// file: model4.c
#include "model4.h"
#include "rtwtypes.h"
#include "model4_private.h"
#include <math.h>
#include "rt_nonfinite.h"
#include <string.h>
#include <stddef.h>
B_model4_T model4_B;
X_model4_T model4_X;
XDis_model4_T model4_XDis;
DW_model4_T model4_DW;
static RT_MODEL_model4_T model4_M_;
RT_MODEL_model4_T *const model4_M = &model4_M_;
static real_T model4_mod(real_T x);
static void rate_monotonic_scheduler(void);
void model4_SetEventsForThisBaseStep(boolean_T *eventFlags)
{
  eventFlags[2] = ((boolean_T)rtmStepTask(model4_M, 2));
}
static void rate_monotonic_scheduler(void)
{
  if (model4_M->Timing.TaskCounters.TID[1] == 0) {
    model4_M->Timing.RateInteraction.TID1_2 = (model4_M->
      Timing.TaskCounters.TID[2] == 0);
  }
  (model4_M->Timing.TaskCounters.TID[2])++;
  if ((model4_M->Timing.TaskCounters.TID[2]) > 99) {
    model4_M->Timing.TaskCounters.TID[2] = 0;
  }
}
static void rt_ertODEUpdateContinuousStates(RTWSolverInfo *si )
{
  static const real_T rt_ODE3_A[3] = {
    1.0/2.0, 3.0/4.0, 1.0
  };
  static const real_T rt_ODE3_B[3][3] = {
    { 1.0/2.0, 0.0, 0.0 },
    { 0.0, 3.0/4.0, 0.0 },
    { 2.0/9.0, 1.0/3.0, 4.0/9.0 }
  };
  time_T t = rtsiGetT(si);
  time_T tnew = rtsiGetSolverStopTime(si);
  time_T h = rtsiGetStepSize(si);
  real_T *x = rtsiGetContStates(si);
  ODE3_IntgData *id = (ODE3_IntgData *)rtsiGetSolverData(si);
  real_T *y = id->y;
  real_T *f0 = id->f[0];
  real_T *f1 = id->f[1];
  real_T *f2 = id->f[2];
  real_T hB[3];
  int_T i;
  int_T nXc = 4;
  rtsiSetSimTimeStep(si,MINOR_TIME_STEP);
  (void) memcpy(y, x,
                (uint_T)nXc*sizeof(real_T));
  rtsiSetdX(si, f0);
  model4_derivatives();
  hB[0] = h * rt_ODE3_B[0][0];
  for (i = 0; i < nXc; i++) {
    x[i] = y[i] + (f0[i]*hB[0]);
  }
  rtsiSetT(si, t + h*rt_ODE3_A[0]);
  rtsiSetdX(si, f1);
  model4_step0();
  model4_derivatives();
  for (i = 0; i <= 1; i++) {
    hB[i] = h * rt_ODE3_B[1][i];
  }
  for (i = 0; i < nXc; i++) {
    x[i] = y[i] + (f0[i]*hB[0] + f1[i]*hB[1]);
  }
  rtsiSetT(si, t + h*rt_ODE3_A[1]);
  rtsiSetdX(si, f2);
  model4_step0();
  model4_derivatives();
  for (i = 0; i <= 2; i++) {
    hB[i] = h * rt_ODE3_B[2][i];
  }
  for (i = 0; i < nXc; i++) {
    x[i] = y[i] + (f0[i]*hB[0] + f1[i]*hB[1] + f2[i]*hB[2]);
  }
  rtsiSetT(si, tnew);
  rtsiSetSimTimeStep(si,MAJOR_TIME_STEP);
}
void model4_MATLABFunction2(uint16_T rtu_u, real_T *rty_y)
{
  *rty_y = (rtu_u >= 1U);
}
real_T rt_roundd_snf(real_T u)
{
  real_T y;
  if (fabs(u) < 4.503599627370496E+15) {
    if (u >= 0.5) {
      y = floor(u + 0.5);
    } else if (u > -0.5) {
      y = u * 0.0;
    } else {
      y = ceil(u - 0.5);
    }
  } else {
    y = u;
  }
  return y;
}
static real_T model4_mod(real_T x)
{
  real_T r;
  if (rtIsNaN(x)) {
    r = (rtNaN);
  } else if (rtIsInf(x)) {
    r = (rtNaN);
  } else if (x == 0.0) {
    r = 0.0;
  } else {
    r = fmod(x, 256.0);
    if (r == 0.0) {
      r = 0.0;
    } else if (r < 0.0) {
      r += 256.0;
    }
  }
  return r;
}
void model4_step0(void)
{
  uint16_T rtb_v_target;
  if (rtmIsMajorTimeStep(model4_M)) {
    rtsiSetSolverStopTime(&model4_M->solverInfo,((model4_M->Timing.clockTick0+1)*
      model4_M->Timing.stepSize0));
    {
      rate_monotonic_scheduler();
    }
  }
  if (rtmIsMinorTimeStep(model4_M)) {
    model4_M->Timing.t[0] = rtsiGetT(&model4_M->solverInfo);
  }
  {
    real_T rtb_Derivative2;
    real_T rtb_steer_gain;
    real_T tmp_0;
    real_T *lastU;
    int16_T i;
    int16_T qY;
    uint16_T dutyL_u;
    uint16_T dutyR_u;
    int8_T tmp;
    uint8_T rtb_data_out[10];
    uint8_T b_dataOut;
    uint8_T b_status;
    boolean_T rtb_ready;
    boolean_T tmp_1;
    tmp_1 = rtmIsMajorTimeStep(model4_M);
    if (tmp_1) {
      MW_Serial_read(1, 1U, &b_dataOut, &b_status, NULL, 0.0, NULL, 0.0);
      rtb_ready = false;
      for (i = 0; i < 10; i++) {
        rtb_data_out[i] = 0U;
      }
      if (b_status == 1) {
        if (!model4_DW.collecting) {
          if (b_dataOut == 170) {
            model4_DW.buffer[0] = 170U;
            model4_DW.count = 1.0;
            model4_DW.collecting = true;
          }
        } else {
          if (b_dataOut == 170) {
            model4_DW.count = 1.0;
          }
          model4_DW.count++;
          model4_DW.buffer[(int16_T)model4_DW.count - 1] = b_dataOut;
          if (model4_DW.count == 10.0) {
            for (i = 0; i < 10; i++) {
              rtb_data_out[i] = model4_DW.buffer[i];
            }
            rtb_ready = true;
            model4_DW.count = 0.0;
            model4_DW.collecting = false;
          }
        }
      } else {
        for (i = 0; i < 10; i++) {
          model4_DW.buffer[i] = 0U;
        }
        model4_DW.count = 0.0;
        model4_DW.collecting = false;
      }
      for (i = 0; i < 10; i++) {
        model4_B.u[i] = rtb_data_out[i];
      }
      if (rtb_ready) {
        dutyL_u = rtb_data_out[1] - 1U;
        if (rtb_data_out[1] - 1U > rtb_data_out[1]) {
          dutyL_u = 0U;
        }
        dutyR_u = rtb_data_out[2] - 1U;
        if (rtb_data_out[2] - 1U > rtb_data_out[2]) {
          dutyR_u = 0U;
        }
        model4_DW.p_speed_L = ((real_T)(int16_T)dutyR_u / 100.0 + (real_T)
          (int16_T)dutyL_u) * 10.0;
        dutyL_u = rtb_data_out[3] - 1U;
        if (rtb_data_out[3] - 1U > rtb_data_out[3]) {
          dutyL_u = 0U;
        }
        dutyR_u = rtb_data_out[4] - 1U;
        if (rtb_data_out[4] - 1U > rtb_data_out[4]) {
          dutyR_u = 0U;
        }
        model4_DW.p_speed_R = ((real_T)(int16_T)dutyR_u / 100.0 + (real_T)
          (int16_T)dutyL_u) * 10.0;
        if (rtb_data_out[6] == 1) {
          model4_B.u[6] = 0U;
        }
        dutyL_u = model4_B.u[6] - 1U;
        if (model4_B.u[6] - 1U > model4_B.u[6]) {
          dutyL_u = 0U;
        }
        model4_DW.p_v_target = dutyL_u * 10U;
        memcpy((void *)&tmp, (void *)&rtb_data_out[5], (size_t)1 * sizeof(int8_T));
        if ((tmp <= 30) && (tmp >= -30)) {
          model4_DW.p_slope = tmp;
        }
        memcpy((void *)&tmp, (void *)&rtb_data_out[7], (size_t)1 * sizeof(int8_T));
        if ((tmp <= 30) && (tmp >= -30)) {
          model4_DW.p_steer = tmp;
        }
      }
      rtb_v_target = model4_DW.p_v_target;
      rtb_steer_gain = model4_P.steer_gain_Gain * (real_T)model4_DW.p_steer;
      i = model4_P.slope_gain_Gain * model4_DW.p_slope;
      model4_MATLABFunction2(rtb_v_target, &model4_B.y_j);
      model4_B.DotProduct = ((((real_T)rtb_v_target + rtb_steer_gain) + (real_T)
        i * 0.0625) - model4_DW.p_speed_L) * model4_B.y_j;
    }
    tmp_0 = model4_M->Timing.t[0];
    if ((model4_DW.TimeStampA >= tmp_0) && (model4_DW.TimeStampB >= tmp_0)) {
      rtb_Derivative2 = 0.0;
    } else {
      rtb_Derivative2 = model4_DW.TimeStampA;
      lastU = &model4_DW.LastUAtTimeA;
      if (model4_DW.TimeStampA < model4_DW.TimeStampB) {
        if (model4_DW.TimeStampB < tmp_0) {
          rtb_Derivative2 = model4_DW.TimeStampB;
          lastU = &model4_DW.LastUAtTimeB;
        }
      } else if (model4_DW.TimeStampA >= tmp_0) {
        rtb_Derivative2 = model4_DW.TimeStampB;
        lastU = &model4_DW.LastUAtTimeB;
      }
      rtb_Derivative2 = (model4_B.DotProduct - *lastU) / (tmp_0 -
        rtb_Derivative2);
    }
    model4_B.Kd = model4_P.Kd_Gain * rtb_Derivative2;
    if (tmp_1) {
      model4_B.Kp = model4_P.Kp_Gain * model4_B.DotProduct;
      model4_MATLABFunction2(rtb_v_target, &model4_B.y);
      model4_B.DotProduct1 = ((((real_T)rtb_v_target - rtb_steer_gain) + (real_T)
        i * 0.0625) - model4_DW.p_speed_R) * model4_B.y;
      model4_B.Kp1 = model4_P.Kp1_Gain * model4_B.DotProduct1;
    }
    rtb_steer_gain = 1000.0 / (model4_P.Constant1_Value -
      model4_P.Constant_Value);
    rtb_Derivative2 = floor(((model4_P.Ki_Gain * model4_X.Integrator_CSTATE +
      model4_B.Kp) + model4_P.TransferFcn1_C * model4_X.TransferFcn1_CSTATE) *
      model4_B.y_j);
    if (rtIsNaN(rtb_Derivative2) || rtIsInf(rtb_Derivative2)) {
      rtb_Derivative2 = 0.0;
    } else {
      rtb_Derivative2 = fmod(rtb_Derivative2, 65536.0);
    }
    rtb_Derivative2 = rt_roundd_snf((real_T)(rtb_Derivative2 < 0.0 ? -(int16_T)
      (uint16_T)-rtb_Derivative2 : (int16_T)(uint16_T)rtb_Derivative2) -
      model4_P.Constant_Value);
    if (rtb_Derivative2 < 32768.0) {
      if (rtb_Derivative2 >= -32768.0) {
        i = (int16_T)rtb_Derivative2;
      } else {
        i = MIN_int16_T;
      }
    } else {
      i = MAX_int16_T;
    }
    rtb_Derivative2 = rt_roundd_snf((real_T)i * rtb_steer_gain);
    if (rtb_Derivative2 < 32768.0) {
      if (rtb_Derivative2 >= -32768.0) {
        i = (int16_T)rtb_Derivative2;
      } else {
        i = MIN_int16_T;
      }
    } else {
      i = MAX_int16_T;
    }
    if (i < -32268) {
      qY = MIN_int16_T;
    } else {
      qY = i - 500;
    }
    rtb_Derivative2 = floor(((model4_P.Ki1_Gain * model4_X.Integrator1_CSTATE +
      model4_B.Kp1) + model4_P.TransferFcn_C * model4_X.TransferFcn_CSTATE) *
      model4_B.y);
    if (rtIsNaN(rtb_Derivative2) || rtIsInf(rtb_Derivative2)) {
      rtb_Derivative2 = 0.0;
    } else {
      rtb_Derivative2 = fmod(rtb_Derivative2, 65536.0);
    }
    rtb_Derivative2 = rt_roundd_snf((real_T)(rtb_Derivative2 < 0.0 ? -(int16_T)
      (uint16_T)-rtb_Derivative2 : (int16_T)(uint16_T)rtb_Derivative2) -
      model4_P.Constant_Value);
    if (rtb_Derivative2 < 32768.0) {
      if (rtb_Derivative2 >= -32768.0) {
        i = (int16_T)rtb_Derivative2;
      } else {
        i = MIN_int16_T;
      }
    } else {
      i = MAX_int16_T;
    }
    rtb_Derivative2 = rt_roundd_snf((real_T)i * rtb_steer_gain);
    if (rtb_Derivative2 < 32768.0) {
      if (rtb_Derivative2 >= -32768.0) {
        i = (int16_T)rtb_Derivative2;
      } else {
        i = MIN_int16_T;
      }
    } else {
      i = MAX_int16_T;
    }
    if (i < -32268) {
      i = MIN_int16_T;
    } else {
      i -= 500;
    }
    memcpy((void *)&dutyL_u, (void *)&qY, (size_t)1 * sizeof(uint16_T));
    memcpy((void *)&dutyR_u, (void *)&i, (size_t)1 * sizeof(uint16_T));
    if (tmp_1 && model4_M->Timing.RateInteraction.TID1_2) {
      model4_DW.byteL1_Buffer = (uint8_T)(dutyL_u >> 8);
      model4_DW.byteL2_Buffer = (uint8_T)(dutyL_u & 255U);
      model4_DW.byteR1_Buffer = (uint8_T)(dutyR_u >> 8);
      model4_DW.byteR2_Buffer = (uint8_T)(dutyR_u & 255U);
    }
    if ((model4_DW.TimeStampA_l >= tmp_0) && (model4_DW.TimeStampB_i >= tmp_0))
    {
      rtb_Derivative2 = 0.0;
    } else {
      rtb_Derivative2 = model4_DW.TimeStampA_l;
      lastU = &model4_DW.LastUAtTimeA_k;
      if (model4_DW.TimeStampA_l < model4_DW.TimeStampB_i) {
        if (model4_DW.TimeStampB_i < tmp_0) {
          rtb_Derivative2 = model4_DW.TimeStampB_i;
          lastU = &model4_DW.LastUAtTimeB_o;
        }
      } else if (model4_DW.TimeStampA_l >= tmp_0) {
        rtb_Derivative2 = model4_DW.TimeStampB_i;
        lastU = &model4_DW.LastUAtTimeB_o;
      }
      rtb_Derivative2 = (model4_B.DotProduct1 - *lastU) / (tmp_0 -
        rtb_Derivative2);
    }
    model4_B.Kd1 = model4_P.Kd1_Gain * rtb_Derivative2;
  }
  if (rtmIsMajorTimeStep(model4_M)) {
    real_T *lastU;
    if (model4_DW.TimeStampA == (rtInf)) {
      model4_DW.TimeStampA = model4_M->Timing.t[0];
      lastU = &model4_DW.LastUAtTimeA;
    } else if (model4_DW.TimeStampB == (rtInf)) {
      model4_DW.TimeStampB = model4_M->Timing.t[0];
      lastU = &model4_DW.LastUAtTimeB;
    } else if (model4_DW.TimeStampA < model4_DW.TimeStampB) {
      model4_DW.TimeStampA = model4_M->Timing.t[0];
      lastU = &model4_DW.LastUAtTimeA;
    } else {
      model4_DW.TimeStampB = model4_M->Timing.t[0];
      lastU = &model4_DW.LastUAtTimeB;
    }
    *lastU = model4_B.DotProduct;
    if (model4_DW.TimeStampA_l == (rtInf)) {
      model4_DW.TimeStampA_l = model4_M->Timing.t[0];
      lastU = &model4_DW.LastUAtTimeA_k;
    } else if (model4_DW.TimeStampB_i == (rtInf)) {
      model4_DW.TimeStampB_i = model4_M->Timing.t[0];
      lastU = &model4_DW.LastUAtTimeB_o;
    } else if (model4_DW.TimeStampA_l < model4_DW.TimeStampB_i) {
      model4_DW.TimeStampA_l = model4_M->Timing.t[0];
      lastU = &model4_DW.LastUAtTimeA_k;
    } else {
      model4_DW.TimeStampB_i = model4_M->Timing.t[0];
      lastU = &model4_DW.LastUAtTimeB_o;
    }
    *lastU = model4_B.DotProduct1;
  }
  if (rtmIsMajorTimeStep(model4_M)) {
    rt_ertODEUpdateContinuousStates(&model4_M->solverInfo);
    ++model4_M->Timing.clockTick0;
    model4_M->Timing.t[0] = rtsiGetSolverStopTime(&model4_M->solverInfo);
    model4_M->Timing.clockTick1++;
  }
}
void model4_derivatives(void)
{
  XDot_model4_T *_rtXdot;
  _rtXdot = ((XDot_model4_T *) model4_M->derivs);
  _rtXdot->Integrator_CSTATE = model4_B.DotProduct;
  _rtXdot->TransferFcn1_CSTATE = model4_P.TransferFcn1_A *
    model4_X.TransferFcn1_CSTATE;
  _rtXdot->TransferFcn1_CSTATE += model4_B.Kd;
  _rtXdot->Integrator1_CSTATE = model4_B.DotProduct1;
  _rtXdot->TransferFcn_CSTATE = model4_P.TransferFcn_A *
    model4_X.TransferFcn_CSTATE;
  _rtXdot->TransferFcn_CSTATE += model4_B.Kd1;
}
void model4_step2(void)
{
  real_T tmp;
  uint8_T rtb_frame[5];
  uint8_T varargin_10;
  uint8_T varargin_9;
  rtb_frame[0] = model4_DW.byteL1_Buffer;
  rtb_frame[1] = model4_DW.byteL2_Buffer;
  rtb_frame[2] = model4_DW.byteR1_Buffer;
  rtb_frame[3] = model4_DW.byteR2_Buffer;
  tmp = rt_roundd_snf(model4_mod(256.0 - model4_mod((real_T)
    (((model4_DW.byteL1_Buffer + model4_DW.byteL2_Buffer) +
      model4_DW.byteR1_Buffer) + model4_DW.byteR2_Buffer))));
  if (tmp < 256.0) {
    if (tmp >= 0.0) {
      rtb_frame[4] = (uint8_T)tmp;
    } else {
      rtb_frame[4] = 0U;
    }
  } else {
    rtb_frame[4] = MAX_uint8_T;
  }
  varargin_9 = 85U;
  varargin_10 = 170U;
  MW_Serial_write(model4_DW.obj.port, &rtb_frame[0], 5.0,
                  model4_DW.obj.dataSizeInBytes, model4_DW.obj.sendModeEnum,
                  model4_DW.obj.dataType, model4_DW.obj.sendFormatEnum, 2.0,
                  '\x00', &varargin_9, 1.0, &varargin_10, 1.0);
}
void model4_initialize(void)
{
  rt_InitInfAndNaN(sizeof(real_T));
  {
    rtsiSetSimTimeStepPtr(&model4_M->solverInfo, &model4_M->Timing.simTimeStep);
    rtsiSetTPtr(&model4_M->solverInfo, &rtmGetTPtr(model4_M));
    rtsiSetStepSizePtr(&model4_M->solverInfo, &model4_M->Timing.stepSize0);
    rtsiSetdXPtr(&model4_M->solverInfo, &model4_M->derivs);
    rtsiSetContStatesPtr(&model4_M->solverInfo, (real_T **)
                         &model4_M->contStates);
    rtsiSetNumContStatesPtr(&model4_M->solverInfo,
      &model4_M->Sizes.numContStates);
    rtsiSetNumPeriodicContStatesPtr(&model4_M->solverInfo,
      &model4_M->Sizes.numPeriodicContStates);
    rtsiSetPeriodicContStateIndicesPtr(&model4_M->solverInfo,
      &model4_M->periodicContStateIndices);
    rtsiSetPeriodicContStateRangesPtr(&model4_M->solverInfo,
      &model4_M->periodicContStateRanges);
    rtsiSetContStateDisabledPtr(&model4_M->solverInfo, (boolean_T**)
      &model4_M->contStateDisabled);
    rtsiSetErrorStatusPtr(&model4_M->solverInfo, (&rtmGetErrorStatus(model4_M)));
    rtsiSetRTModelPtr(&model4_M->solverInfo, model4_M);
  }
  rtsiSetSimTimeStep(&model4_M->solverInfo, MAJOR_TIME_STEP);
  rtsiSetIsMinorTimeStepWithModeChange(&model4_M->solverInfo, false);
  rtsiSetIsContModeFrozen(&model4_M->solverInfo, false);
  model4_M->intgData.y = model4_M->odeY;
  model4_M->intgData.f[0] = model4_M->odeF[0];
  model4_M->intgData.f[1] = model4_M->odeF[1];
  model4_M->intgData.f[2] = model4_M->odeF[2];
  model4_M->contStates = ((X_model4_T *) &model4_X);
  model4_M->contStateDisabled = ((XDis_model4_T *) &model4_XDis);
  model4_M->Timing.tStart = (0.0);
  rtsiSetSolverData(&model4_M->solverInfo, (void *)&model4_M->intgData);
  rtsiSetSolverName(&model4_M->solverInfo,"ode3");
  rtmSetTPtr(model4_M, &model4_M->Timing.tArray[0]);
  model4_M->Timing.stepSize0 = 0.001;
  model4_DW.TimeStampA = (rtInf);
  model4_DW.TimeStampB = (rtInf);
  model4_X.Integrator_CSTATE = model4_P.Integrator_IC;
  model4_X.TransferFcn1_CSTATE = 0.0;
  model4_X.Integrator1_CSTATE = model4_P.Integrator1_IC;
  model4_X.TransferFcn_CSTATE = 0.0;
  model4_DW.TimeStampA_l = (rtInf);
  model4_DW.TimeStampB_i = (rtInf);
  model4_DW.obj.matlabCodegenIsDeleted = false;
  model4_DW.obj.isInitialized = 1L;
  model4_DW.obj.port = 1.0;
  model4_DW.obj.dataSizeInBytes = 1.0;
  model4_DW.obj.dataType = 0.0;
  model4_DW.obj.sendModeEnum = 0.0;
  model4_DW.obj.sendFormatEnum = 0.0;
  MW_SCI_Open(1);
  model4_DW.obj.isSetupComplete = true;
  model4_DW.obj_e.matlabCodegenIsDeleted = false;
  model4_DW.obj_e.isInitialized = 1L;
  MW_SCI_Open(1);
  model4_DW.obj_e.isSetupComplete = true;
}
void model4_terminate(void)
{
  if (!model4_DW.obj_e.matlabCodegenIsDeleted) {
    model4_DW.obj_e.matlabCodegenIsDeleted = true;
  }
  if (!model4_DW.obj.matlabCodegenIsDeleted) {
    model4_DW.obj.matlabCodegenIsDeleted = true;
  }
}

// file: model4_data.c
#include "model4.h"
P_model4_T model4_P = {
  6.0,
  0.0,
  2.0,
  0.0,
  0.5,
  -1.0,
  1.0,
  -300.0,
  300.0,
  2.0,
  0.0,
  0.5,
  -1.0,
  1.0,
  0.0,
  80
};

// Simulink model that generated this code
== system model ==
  Subsystem#1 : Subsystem  <- 1: MATLABFunction#1, 2: MATLABFunction#1/2, 3: MATLABFunction#1/3, 4: MATLABFunction#1/4
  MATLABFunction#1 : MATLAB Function  <- 1: DotProduct#1, 2: DotProduct#2, 3: Constant, 4: Constant1
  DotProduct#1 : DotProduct  <- 1: MATLABFunction2, 2: Sum#1
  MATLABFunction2 : MATLAB Function  <- 1: MATLABFunction#2/4
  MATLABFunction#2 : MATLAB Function  <- 1: MATLABFunction#3, 2: MATLABFunction#3/2
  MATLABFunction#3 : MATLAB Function  <- 1: SerialReceive#1, 2: SerialReceive#1/2
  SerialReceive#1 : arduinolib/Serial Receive
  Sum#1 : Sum  Inputs=+++  <- 1: Kp, 2: Ki, 3: TransferFcn1
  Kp : Gain  Gain=2  <- 1: DotProduct
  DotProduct : DotProduct  <- 1: MATLABFunction2, 2: Sum#2
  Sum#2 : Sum  Inputs=+-  <- 1: Sum#3, 2: MATLABFunction#2/2
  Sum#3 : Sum  Inputs=+++  <- 1: MATLABFunction#2/4, 2: steer_gain, 3: slope_gain
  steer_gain : Gain  Gain=6  <- 1: MATLABFunction#2/6
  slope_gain : Gain  Gain=5  <- 1: MATLABFunction#2/5
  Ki : Gain  Gain=0.5  <- 1: Integrator
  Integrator : Integrator  <- 1: DotProduct
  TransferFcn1 : TransferFcn  Denominator=[1 1]  <- 1: Kd
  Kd : Gain  Gain=0  <- 1: Derivative#1
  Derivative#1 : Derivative  <- 1: DotProduct
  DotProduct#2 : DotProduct  <- 1: MATLABFunction#4, 2: Sum#4
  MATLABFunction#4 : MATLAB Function  <- 1: MATLABFunction#2/4
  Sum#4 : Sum  Inputs=+++  <- 1: Kp1, 2: Ki1, 3: TransferFcn
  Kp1 : Gain  Gain=2  <- 1: DotProduct1
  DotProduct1 : DotProduct  <- 1: MATLABFunction#4, 2: Sum#5
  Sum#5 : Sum  Inputs=+-  <- 1: Sum#6, 2: MATLABFunction#2/3
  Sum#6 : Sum  Inputs=+-+  <- 1: MATLABFunction#2/4, 2: steer_gain, 3: slope_gain
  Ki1 : Gain  Gain=0.5  <- 1: Integrator1
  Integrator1 : Integrator  <- 1: DotProduct1
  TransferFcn : TransferFcn  Denominator=[1 1]  <- 1: Kd1
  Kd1 : Gain  Gain=0  <- 1: Derivative2
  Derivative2 : Derivative  <- 1: DotProduct1
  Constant : Constant  Value=-300
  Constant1 : Constant  Value=300
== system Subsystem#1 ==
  Inport#1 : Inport
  Inport#2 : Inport
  Inport#3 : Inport
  Inport#4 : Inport
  SerialTransmit#1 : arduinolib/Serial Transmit  <- 1: MATLABFunction#5
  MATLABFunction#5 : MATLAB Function  <- 1: Inport#1, 2: Inport#2, 3: Inport#3, 4: Inport#4
== matlab function MATLABFunction#1 ==
function [byteL1, byteL2, byteR1, byteR2] = encode_pwm_duty(PID_L, PID_R, u_min, u_max)
%#codegen

% [-1000, 1000] 범위로 선형 매핑
scale = 1000 / (u_max - u_min);
dutyL = int16(round((PID_L - u_min) * scale - 500));
dutyR = int16(round((PID_R - u_min) * scale - 500));

% uint16로 안전 변환 (비트 연산 위해)
dutyL_u = uint16(typecast(dutyL, 'uint16'));
dutyL_u = dutyL_u(1);
dutyR_u = uint16(typecast(dutyR, 'uint16'));
dutyR_u = dutyR_u(1);
% MSB / LSB 분리
byteL1 = uint8(bitshift(dutyL_u, -8));  % MSB
byteL2 = uint8(bitand(dutyL_u, 255));   % LSB

byteR1 = uint8(bitshift(dutyR_u, -8));
byteR2 = uint8(bitand(dutyR_u, 255));

% function [byteL1, byteL2, byteR1, byteR2] = encode_pwm_duty(PID_L, PID_R, u_min, u_max)
% % PID_L, PID_R : PID 제어기 출력값 (실수형)
% % u_min, u_max : PID 출력 예상 범위 (예: -4050 ~ +4050)
% 
% % 매핑 대상 범위
% min_duty = -1000;
% max_duty = 1000;
% 
% %% 매핑 함수 정의
% map_to_range = @(u) ((u - u_min) / (u_max - u_min)) * (max_duty - min_duty) + min_duty;
% 
% % 매핑 수행
% dutyL = int16(round(map_to_range(PID_L)));  % 정수로 변환
% dutyR = int16(round(map_to_range(PID_R)));
% 
% % MSB/LSB 분리
% byteL2 = bitand(dutyL, 255);         % LSB
% byteL1 = bitshift(dutyL, -8);        % MSB
% 
% byteR2 = bitand(dutyR, 255);
% byteR1 = bitshift(dutyR, -8);

== matlab function MATLABFunction2 ==
function y = fcn(u)

if u<1 && u > -1
    y=0;
else
    y=1;
end

== matlab function MATLABFunction#2 ==
function [valid, speed_L, speed_R, v_target, slope, steer, crc] =  Arduino_Input2( ready, u)
% UART 패킷 파서 (persistent 방식으로 이전 값 유지)
% u: [10x1] uint8, 패킷 데이터
% ready: 패킷 유효 신호

%#codegen

% 이전 출력값 저장용 persistent 변수
persistent p_valid p_speed_L p_speed_R p_v_target p_slope p_steer p_crc
 
% 초기화 (최초 실행 시)
if isempty(p_valid)
    p_valid = false;
    p_speed_L = 0.0;
    p_speed_R = 0.0;
    p_v_target = uint16(0);
    p_slope = int8(0);
    p_steer = int8(0);
    p_crc = uint8(0);
end

% 새로운 데이터가 들어왔을 경우만 업데이트
if ready == 1
    % data_sum = uint16((2)) + uint16(u(3)) + uint16(u(4)) + uint16(u(5)) + uint16(u(6)) + uint16(u(7)) + uint16(u(8)) + uint16(u(9));
    % if (0xFF & data_sum) == 0
        p_valid = true;
        p_speed_L = (double(u(2)-1) + double(u(3)-1)/100)*10;
        p_speed_R = (double(u(4)-1) + double(u(5)-1)/100)*10;
        if u(7)==1
            u(7)=u(7)-1;
        end
        p_v_target = uint16(u(7)-1)*10;
        tmp = typecast(u(6), 'int8'); tmp = tmp(1);
        if tmp <= int8(30) && tmp >= int8(-30)
            p_slope = tmp;
        end
        tmp = typecast(u(8), 'int8'); tmp = tmp(1);
        if  tmp <= int8(30) && tmp >= int8(-30)
            p_steer = tmp;
        end
        p_crc = u(9);
    % end
end

% 항상 마지막 유효 출력 반환
valid     = p_valid;
speed_L   = p_speed_L;
speed_R   = p_speed_R;
v_target  = p_v_target;
slope     = p_slope;
steer     = p_steer;
crc       = p_crc;

== matlab function MATLABFunction#3 ==
function [ready, data_out] = uart_parser(byte_in, status)
% UART 프레임 수신기 (Start Byte = 0xAA, Total = 10 bytes)
% 입력: byte_in - 1바이트씩 들어오는 uint8
% 입력: status - Serial Receive의 상태 (1이면 수신 성공)
% 출력: ready - 1이면 패킷 파싱 완료
% 출력: data_out - [1x10] uint8, 패킷 데이터

persistent buffer count collecting

if isempty(buffer)
    buffer = zeros(1, 10, 'uint8');
    count = 0;
    collecting = false;
end

ready = false;
data_out = zeros(1,10,'uint8');

if status == 1
    if ~collecting
        % 아직 수집 시작 전 → start byte 찾기
        if byte_in == hex2dec('AA')
            buffer(1) = byte_in;
            count = 1;
            collecting = true;
        end
    else
        if byte_in == hex2dec('AA')
            count = 1;
        end
        % 수집 중
        count = count + 1;
        buffer(count) = byte_in;

        if count == 10
            data_out = buffer;
            ready = true;
            count = 0;
            collecting = false;
        end
    end
else
    % if count~=0
    %     count = count + 1;
    %     buffer(count) = uint8(0);
    %     if count == 10
    %         data_out = buffer;
    %         ready = true;
    %         count = 0;
    %         collecting = false;
    %     end
    % else
        buffer = zeros(1, 10, 'uint8');
        count = 0;
        collecting = false;
    % end
end

== matlab function MATLABFunction#4 ==
function y = fcn(u)

if u<1 && u > -1
    y=0;
else
    y=1;
end

== matlab function MATLABFunction#5 ==
function frame = makeFrame(L1,L2,R1,R2)
% 입력:
%   vL, vR : 좌/우 목표 속도 (실수, cm/s 단위)
% 출력:
%   frame : 7-byte UART 전송 프레임 (uint8 벡터)
    frame = zeros(5,1,'uint8');  % 7바이트 프레임

    % 2-3. 목표속도_L (정수 + 소수)
    frame(1) = uint8(L1);                       % 정수부
    frame(2) = uint8(L2);       % 소수부 (소수점 둘째 자리까지)

    % 4-5. 목표속도_R (정수 + 소수)
    frame(3) = uint8(R1);                       % 정수부
    frame(4) = uint8(R2);       % 소수부

    % 6. CRC: 256 - (sum of byte 1~5) % 256
    crc = mod(sum(double(frame(1:5))), 256);
    frame(5) = uint8(mod(256 - crc, 256));
    
end
